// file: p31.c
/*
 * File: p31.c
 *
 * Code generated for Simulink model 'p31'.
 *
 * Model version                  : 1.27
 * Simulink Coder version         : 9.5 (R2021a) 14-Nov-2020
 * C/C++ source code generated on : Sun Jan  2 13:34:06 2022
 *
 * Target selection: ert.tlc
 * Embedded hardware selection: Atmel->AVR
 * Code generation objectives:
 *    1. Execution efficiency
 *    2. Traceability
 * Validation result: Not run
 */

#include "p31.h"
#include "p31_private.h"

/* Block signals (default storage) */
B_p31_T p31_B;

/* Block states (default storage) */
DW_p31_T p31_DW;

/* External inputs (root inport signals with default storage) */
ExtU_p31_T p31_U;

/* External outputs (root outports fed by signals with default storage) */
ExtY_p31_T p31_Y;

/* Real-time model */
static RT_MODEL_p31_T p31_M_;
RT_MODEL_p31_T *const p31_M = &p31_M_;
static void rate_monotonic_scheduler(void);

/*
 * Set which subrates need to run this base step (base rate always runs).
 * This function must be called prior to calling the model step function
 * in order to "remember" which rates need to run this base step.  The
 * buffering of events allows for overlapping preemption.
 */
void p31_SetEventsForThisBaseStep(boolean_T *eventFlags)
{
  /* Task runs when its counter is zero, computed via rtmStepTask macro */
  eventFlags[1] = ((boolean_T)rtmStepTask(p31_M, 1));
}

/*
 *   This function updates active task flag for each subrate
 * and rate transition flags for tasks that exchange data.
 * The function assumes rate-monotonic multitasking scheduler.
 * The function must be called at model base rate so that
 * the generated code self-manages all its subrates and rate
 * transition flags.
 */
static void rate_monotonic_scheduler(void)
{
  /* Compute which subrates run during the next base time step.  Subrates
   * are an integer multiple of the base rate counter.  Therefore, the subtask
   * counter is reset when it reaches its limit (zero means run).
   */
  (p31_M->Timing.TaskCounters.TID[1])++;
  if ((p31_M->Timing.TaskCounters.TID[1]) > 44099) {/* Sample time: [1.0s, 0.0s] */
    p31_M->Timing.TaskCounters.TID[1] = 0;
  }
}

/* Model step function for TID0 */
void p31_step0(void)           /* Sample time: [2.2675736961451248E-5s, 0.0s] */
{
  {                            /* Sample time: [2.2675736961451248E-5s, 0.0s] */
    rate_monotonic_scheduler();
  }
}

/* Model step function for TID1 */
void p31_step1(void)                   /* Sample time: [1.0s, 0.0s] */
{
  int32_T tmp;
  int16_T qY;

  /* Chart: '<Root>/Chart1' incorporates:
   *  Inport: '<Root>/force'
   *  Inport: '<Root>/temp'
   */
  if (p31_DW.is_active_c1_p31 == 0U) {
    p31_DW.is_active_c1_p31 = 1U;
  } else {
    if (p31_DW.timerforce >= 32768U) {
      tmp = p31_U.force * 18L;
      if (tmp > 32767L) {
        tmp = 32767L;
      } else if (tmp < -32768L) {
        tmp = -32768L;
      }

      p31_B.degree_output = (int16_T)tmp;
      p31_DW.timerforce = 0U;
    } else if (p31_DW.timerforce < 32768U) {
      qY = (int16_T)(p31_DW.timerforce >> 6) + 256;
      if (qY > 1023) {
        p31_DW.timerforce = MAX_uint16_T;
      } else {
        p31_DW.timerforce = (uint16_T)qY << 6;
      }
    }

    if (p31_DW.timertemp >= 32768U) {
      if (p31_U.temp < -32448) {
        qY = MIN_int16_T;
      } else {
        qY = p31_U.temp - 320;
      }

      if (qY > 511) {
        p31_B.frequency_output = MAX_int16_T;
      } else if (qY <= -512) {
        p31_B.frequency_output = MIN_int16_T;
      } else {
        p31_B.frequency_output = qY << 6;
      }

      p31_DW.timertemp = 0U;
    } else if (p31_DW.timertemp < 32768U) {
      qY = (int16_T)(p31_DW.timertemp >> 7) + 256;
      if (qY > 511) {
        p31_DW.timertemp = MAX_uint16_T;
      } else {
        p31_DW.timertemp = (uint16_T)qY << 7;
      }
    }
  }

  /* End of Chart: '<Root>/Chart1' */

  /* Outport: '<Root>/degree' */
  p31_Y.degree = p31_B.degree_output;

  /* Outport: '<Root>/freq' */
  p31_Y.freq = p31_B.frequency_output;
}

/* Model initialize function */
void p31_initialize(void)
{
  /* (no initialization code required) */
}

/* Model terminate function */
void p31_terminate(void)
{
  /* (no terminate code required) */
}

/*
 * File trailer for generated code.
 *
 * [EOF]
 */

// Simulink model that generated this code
simulink model "p31"  (R2021a)
settings: Solver=FixedStepDiscrete  StartTime=0.0  StopTime=5  FixedStep=1/44100  RelTol=1e-3  EnableMultiTasking=on

== system p31 ==
  temp : Inport  OutDataTypeStr=fixdt(1,16,4)
  force : Inport  Port=2  OutDataTypeStr=fixdt(1,16,4)
  Chart1 : Stateflow chart  TreatAsAtomicUnit=on
  degree : Outport
  freq : Outport  Port=2
  wires:
  force/1 -> Chart1/2(force_input)
  temp/1 -> Chart1/1(temp_input)
  Chart1/1(degree_output) -> degree/1
  Chart1/2(frequency_output) -> freq/1

== stateflow chart p31/Chart1 ==
  settings: updateMethod=DISCRETE  sampleTime=1
  state state2 [parallel]
    settings: executionOrder=1
    state fsr402
      entry:
    (default) -> fsr402
    fsr402 -> fsr402 [order 2] : [timerforce<2]{timerforce = timerforce+1;}
    fsr402 -> fsr402 [order 1] : [timerforce>=2]{degree_output = (force_input * 18);timerforce =0;}
  state state [parallel]
    settings: executionOrder=2
    state temp36
    (default) -> temp36
    temp36 -> temp36 [order 2] : [timertemp<1]{timertemp = timertemp+1;}
    temp36 -> temp36 [order 1] : [timertemp>=1]{frequency_output = (temp_input-20);   timertemp = 0;}
  (default) -> state2 [order 2]
  (default) -> state [order 1]
  data: temp_input input fixdt(1,16,4); force_input input fixdt(1,16,4); degree_output output fixdt(1,16,4); frequency_output output fixdt(1,16,10); timerforce local fixdt(0,16,14); timertemp local fixdt(0,16,15)
  data timerforce settings: updateMethod=SF_CONTINUOUS_TIME_DATA
  data timertemp settings: updateMethod=SF_CONTINUOUS_TIME_DATA
